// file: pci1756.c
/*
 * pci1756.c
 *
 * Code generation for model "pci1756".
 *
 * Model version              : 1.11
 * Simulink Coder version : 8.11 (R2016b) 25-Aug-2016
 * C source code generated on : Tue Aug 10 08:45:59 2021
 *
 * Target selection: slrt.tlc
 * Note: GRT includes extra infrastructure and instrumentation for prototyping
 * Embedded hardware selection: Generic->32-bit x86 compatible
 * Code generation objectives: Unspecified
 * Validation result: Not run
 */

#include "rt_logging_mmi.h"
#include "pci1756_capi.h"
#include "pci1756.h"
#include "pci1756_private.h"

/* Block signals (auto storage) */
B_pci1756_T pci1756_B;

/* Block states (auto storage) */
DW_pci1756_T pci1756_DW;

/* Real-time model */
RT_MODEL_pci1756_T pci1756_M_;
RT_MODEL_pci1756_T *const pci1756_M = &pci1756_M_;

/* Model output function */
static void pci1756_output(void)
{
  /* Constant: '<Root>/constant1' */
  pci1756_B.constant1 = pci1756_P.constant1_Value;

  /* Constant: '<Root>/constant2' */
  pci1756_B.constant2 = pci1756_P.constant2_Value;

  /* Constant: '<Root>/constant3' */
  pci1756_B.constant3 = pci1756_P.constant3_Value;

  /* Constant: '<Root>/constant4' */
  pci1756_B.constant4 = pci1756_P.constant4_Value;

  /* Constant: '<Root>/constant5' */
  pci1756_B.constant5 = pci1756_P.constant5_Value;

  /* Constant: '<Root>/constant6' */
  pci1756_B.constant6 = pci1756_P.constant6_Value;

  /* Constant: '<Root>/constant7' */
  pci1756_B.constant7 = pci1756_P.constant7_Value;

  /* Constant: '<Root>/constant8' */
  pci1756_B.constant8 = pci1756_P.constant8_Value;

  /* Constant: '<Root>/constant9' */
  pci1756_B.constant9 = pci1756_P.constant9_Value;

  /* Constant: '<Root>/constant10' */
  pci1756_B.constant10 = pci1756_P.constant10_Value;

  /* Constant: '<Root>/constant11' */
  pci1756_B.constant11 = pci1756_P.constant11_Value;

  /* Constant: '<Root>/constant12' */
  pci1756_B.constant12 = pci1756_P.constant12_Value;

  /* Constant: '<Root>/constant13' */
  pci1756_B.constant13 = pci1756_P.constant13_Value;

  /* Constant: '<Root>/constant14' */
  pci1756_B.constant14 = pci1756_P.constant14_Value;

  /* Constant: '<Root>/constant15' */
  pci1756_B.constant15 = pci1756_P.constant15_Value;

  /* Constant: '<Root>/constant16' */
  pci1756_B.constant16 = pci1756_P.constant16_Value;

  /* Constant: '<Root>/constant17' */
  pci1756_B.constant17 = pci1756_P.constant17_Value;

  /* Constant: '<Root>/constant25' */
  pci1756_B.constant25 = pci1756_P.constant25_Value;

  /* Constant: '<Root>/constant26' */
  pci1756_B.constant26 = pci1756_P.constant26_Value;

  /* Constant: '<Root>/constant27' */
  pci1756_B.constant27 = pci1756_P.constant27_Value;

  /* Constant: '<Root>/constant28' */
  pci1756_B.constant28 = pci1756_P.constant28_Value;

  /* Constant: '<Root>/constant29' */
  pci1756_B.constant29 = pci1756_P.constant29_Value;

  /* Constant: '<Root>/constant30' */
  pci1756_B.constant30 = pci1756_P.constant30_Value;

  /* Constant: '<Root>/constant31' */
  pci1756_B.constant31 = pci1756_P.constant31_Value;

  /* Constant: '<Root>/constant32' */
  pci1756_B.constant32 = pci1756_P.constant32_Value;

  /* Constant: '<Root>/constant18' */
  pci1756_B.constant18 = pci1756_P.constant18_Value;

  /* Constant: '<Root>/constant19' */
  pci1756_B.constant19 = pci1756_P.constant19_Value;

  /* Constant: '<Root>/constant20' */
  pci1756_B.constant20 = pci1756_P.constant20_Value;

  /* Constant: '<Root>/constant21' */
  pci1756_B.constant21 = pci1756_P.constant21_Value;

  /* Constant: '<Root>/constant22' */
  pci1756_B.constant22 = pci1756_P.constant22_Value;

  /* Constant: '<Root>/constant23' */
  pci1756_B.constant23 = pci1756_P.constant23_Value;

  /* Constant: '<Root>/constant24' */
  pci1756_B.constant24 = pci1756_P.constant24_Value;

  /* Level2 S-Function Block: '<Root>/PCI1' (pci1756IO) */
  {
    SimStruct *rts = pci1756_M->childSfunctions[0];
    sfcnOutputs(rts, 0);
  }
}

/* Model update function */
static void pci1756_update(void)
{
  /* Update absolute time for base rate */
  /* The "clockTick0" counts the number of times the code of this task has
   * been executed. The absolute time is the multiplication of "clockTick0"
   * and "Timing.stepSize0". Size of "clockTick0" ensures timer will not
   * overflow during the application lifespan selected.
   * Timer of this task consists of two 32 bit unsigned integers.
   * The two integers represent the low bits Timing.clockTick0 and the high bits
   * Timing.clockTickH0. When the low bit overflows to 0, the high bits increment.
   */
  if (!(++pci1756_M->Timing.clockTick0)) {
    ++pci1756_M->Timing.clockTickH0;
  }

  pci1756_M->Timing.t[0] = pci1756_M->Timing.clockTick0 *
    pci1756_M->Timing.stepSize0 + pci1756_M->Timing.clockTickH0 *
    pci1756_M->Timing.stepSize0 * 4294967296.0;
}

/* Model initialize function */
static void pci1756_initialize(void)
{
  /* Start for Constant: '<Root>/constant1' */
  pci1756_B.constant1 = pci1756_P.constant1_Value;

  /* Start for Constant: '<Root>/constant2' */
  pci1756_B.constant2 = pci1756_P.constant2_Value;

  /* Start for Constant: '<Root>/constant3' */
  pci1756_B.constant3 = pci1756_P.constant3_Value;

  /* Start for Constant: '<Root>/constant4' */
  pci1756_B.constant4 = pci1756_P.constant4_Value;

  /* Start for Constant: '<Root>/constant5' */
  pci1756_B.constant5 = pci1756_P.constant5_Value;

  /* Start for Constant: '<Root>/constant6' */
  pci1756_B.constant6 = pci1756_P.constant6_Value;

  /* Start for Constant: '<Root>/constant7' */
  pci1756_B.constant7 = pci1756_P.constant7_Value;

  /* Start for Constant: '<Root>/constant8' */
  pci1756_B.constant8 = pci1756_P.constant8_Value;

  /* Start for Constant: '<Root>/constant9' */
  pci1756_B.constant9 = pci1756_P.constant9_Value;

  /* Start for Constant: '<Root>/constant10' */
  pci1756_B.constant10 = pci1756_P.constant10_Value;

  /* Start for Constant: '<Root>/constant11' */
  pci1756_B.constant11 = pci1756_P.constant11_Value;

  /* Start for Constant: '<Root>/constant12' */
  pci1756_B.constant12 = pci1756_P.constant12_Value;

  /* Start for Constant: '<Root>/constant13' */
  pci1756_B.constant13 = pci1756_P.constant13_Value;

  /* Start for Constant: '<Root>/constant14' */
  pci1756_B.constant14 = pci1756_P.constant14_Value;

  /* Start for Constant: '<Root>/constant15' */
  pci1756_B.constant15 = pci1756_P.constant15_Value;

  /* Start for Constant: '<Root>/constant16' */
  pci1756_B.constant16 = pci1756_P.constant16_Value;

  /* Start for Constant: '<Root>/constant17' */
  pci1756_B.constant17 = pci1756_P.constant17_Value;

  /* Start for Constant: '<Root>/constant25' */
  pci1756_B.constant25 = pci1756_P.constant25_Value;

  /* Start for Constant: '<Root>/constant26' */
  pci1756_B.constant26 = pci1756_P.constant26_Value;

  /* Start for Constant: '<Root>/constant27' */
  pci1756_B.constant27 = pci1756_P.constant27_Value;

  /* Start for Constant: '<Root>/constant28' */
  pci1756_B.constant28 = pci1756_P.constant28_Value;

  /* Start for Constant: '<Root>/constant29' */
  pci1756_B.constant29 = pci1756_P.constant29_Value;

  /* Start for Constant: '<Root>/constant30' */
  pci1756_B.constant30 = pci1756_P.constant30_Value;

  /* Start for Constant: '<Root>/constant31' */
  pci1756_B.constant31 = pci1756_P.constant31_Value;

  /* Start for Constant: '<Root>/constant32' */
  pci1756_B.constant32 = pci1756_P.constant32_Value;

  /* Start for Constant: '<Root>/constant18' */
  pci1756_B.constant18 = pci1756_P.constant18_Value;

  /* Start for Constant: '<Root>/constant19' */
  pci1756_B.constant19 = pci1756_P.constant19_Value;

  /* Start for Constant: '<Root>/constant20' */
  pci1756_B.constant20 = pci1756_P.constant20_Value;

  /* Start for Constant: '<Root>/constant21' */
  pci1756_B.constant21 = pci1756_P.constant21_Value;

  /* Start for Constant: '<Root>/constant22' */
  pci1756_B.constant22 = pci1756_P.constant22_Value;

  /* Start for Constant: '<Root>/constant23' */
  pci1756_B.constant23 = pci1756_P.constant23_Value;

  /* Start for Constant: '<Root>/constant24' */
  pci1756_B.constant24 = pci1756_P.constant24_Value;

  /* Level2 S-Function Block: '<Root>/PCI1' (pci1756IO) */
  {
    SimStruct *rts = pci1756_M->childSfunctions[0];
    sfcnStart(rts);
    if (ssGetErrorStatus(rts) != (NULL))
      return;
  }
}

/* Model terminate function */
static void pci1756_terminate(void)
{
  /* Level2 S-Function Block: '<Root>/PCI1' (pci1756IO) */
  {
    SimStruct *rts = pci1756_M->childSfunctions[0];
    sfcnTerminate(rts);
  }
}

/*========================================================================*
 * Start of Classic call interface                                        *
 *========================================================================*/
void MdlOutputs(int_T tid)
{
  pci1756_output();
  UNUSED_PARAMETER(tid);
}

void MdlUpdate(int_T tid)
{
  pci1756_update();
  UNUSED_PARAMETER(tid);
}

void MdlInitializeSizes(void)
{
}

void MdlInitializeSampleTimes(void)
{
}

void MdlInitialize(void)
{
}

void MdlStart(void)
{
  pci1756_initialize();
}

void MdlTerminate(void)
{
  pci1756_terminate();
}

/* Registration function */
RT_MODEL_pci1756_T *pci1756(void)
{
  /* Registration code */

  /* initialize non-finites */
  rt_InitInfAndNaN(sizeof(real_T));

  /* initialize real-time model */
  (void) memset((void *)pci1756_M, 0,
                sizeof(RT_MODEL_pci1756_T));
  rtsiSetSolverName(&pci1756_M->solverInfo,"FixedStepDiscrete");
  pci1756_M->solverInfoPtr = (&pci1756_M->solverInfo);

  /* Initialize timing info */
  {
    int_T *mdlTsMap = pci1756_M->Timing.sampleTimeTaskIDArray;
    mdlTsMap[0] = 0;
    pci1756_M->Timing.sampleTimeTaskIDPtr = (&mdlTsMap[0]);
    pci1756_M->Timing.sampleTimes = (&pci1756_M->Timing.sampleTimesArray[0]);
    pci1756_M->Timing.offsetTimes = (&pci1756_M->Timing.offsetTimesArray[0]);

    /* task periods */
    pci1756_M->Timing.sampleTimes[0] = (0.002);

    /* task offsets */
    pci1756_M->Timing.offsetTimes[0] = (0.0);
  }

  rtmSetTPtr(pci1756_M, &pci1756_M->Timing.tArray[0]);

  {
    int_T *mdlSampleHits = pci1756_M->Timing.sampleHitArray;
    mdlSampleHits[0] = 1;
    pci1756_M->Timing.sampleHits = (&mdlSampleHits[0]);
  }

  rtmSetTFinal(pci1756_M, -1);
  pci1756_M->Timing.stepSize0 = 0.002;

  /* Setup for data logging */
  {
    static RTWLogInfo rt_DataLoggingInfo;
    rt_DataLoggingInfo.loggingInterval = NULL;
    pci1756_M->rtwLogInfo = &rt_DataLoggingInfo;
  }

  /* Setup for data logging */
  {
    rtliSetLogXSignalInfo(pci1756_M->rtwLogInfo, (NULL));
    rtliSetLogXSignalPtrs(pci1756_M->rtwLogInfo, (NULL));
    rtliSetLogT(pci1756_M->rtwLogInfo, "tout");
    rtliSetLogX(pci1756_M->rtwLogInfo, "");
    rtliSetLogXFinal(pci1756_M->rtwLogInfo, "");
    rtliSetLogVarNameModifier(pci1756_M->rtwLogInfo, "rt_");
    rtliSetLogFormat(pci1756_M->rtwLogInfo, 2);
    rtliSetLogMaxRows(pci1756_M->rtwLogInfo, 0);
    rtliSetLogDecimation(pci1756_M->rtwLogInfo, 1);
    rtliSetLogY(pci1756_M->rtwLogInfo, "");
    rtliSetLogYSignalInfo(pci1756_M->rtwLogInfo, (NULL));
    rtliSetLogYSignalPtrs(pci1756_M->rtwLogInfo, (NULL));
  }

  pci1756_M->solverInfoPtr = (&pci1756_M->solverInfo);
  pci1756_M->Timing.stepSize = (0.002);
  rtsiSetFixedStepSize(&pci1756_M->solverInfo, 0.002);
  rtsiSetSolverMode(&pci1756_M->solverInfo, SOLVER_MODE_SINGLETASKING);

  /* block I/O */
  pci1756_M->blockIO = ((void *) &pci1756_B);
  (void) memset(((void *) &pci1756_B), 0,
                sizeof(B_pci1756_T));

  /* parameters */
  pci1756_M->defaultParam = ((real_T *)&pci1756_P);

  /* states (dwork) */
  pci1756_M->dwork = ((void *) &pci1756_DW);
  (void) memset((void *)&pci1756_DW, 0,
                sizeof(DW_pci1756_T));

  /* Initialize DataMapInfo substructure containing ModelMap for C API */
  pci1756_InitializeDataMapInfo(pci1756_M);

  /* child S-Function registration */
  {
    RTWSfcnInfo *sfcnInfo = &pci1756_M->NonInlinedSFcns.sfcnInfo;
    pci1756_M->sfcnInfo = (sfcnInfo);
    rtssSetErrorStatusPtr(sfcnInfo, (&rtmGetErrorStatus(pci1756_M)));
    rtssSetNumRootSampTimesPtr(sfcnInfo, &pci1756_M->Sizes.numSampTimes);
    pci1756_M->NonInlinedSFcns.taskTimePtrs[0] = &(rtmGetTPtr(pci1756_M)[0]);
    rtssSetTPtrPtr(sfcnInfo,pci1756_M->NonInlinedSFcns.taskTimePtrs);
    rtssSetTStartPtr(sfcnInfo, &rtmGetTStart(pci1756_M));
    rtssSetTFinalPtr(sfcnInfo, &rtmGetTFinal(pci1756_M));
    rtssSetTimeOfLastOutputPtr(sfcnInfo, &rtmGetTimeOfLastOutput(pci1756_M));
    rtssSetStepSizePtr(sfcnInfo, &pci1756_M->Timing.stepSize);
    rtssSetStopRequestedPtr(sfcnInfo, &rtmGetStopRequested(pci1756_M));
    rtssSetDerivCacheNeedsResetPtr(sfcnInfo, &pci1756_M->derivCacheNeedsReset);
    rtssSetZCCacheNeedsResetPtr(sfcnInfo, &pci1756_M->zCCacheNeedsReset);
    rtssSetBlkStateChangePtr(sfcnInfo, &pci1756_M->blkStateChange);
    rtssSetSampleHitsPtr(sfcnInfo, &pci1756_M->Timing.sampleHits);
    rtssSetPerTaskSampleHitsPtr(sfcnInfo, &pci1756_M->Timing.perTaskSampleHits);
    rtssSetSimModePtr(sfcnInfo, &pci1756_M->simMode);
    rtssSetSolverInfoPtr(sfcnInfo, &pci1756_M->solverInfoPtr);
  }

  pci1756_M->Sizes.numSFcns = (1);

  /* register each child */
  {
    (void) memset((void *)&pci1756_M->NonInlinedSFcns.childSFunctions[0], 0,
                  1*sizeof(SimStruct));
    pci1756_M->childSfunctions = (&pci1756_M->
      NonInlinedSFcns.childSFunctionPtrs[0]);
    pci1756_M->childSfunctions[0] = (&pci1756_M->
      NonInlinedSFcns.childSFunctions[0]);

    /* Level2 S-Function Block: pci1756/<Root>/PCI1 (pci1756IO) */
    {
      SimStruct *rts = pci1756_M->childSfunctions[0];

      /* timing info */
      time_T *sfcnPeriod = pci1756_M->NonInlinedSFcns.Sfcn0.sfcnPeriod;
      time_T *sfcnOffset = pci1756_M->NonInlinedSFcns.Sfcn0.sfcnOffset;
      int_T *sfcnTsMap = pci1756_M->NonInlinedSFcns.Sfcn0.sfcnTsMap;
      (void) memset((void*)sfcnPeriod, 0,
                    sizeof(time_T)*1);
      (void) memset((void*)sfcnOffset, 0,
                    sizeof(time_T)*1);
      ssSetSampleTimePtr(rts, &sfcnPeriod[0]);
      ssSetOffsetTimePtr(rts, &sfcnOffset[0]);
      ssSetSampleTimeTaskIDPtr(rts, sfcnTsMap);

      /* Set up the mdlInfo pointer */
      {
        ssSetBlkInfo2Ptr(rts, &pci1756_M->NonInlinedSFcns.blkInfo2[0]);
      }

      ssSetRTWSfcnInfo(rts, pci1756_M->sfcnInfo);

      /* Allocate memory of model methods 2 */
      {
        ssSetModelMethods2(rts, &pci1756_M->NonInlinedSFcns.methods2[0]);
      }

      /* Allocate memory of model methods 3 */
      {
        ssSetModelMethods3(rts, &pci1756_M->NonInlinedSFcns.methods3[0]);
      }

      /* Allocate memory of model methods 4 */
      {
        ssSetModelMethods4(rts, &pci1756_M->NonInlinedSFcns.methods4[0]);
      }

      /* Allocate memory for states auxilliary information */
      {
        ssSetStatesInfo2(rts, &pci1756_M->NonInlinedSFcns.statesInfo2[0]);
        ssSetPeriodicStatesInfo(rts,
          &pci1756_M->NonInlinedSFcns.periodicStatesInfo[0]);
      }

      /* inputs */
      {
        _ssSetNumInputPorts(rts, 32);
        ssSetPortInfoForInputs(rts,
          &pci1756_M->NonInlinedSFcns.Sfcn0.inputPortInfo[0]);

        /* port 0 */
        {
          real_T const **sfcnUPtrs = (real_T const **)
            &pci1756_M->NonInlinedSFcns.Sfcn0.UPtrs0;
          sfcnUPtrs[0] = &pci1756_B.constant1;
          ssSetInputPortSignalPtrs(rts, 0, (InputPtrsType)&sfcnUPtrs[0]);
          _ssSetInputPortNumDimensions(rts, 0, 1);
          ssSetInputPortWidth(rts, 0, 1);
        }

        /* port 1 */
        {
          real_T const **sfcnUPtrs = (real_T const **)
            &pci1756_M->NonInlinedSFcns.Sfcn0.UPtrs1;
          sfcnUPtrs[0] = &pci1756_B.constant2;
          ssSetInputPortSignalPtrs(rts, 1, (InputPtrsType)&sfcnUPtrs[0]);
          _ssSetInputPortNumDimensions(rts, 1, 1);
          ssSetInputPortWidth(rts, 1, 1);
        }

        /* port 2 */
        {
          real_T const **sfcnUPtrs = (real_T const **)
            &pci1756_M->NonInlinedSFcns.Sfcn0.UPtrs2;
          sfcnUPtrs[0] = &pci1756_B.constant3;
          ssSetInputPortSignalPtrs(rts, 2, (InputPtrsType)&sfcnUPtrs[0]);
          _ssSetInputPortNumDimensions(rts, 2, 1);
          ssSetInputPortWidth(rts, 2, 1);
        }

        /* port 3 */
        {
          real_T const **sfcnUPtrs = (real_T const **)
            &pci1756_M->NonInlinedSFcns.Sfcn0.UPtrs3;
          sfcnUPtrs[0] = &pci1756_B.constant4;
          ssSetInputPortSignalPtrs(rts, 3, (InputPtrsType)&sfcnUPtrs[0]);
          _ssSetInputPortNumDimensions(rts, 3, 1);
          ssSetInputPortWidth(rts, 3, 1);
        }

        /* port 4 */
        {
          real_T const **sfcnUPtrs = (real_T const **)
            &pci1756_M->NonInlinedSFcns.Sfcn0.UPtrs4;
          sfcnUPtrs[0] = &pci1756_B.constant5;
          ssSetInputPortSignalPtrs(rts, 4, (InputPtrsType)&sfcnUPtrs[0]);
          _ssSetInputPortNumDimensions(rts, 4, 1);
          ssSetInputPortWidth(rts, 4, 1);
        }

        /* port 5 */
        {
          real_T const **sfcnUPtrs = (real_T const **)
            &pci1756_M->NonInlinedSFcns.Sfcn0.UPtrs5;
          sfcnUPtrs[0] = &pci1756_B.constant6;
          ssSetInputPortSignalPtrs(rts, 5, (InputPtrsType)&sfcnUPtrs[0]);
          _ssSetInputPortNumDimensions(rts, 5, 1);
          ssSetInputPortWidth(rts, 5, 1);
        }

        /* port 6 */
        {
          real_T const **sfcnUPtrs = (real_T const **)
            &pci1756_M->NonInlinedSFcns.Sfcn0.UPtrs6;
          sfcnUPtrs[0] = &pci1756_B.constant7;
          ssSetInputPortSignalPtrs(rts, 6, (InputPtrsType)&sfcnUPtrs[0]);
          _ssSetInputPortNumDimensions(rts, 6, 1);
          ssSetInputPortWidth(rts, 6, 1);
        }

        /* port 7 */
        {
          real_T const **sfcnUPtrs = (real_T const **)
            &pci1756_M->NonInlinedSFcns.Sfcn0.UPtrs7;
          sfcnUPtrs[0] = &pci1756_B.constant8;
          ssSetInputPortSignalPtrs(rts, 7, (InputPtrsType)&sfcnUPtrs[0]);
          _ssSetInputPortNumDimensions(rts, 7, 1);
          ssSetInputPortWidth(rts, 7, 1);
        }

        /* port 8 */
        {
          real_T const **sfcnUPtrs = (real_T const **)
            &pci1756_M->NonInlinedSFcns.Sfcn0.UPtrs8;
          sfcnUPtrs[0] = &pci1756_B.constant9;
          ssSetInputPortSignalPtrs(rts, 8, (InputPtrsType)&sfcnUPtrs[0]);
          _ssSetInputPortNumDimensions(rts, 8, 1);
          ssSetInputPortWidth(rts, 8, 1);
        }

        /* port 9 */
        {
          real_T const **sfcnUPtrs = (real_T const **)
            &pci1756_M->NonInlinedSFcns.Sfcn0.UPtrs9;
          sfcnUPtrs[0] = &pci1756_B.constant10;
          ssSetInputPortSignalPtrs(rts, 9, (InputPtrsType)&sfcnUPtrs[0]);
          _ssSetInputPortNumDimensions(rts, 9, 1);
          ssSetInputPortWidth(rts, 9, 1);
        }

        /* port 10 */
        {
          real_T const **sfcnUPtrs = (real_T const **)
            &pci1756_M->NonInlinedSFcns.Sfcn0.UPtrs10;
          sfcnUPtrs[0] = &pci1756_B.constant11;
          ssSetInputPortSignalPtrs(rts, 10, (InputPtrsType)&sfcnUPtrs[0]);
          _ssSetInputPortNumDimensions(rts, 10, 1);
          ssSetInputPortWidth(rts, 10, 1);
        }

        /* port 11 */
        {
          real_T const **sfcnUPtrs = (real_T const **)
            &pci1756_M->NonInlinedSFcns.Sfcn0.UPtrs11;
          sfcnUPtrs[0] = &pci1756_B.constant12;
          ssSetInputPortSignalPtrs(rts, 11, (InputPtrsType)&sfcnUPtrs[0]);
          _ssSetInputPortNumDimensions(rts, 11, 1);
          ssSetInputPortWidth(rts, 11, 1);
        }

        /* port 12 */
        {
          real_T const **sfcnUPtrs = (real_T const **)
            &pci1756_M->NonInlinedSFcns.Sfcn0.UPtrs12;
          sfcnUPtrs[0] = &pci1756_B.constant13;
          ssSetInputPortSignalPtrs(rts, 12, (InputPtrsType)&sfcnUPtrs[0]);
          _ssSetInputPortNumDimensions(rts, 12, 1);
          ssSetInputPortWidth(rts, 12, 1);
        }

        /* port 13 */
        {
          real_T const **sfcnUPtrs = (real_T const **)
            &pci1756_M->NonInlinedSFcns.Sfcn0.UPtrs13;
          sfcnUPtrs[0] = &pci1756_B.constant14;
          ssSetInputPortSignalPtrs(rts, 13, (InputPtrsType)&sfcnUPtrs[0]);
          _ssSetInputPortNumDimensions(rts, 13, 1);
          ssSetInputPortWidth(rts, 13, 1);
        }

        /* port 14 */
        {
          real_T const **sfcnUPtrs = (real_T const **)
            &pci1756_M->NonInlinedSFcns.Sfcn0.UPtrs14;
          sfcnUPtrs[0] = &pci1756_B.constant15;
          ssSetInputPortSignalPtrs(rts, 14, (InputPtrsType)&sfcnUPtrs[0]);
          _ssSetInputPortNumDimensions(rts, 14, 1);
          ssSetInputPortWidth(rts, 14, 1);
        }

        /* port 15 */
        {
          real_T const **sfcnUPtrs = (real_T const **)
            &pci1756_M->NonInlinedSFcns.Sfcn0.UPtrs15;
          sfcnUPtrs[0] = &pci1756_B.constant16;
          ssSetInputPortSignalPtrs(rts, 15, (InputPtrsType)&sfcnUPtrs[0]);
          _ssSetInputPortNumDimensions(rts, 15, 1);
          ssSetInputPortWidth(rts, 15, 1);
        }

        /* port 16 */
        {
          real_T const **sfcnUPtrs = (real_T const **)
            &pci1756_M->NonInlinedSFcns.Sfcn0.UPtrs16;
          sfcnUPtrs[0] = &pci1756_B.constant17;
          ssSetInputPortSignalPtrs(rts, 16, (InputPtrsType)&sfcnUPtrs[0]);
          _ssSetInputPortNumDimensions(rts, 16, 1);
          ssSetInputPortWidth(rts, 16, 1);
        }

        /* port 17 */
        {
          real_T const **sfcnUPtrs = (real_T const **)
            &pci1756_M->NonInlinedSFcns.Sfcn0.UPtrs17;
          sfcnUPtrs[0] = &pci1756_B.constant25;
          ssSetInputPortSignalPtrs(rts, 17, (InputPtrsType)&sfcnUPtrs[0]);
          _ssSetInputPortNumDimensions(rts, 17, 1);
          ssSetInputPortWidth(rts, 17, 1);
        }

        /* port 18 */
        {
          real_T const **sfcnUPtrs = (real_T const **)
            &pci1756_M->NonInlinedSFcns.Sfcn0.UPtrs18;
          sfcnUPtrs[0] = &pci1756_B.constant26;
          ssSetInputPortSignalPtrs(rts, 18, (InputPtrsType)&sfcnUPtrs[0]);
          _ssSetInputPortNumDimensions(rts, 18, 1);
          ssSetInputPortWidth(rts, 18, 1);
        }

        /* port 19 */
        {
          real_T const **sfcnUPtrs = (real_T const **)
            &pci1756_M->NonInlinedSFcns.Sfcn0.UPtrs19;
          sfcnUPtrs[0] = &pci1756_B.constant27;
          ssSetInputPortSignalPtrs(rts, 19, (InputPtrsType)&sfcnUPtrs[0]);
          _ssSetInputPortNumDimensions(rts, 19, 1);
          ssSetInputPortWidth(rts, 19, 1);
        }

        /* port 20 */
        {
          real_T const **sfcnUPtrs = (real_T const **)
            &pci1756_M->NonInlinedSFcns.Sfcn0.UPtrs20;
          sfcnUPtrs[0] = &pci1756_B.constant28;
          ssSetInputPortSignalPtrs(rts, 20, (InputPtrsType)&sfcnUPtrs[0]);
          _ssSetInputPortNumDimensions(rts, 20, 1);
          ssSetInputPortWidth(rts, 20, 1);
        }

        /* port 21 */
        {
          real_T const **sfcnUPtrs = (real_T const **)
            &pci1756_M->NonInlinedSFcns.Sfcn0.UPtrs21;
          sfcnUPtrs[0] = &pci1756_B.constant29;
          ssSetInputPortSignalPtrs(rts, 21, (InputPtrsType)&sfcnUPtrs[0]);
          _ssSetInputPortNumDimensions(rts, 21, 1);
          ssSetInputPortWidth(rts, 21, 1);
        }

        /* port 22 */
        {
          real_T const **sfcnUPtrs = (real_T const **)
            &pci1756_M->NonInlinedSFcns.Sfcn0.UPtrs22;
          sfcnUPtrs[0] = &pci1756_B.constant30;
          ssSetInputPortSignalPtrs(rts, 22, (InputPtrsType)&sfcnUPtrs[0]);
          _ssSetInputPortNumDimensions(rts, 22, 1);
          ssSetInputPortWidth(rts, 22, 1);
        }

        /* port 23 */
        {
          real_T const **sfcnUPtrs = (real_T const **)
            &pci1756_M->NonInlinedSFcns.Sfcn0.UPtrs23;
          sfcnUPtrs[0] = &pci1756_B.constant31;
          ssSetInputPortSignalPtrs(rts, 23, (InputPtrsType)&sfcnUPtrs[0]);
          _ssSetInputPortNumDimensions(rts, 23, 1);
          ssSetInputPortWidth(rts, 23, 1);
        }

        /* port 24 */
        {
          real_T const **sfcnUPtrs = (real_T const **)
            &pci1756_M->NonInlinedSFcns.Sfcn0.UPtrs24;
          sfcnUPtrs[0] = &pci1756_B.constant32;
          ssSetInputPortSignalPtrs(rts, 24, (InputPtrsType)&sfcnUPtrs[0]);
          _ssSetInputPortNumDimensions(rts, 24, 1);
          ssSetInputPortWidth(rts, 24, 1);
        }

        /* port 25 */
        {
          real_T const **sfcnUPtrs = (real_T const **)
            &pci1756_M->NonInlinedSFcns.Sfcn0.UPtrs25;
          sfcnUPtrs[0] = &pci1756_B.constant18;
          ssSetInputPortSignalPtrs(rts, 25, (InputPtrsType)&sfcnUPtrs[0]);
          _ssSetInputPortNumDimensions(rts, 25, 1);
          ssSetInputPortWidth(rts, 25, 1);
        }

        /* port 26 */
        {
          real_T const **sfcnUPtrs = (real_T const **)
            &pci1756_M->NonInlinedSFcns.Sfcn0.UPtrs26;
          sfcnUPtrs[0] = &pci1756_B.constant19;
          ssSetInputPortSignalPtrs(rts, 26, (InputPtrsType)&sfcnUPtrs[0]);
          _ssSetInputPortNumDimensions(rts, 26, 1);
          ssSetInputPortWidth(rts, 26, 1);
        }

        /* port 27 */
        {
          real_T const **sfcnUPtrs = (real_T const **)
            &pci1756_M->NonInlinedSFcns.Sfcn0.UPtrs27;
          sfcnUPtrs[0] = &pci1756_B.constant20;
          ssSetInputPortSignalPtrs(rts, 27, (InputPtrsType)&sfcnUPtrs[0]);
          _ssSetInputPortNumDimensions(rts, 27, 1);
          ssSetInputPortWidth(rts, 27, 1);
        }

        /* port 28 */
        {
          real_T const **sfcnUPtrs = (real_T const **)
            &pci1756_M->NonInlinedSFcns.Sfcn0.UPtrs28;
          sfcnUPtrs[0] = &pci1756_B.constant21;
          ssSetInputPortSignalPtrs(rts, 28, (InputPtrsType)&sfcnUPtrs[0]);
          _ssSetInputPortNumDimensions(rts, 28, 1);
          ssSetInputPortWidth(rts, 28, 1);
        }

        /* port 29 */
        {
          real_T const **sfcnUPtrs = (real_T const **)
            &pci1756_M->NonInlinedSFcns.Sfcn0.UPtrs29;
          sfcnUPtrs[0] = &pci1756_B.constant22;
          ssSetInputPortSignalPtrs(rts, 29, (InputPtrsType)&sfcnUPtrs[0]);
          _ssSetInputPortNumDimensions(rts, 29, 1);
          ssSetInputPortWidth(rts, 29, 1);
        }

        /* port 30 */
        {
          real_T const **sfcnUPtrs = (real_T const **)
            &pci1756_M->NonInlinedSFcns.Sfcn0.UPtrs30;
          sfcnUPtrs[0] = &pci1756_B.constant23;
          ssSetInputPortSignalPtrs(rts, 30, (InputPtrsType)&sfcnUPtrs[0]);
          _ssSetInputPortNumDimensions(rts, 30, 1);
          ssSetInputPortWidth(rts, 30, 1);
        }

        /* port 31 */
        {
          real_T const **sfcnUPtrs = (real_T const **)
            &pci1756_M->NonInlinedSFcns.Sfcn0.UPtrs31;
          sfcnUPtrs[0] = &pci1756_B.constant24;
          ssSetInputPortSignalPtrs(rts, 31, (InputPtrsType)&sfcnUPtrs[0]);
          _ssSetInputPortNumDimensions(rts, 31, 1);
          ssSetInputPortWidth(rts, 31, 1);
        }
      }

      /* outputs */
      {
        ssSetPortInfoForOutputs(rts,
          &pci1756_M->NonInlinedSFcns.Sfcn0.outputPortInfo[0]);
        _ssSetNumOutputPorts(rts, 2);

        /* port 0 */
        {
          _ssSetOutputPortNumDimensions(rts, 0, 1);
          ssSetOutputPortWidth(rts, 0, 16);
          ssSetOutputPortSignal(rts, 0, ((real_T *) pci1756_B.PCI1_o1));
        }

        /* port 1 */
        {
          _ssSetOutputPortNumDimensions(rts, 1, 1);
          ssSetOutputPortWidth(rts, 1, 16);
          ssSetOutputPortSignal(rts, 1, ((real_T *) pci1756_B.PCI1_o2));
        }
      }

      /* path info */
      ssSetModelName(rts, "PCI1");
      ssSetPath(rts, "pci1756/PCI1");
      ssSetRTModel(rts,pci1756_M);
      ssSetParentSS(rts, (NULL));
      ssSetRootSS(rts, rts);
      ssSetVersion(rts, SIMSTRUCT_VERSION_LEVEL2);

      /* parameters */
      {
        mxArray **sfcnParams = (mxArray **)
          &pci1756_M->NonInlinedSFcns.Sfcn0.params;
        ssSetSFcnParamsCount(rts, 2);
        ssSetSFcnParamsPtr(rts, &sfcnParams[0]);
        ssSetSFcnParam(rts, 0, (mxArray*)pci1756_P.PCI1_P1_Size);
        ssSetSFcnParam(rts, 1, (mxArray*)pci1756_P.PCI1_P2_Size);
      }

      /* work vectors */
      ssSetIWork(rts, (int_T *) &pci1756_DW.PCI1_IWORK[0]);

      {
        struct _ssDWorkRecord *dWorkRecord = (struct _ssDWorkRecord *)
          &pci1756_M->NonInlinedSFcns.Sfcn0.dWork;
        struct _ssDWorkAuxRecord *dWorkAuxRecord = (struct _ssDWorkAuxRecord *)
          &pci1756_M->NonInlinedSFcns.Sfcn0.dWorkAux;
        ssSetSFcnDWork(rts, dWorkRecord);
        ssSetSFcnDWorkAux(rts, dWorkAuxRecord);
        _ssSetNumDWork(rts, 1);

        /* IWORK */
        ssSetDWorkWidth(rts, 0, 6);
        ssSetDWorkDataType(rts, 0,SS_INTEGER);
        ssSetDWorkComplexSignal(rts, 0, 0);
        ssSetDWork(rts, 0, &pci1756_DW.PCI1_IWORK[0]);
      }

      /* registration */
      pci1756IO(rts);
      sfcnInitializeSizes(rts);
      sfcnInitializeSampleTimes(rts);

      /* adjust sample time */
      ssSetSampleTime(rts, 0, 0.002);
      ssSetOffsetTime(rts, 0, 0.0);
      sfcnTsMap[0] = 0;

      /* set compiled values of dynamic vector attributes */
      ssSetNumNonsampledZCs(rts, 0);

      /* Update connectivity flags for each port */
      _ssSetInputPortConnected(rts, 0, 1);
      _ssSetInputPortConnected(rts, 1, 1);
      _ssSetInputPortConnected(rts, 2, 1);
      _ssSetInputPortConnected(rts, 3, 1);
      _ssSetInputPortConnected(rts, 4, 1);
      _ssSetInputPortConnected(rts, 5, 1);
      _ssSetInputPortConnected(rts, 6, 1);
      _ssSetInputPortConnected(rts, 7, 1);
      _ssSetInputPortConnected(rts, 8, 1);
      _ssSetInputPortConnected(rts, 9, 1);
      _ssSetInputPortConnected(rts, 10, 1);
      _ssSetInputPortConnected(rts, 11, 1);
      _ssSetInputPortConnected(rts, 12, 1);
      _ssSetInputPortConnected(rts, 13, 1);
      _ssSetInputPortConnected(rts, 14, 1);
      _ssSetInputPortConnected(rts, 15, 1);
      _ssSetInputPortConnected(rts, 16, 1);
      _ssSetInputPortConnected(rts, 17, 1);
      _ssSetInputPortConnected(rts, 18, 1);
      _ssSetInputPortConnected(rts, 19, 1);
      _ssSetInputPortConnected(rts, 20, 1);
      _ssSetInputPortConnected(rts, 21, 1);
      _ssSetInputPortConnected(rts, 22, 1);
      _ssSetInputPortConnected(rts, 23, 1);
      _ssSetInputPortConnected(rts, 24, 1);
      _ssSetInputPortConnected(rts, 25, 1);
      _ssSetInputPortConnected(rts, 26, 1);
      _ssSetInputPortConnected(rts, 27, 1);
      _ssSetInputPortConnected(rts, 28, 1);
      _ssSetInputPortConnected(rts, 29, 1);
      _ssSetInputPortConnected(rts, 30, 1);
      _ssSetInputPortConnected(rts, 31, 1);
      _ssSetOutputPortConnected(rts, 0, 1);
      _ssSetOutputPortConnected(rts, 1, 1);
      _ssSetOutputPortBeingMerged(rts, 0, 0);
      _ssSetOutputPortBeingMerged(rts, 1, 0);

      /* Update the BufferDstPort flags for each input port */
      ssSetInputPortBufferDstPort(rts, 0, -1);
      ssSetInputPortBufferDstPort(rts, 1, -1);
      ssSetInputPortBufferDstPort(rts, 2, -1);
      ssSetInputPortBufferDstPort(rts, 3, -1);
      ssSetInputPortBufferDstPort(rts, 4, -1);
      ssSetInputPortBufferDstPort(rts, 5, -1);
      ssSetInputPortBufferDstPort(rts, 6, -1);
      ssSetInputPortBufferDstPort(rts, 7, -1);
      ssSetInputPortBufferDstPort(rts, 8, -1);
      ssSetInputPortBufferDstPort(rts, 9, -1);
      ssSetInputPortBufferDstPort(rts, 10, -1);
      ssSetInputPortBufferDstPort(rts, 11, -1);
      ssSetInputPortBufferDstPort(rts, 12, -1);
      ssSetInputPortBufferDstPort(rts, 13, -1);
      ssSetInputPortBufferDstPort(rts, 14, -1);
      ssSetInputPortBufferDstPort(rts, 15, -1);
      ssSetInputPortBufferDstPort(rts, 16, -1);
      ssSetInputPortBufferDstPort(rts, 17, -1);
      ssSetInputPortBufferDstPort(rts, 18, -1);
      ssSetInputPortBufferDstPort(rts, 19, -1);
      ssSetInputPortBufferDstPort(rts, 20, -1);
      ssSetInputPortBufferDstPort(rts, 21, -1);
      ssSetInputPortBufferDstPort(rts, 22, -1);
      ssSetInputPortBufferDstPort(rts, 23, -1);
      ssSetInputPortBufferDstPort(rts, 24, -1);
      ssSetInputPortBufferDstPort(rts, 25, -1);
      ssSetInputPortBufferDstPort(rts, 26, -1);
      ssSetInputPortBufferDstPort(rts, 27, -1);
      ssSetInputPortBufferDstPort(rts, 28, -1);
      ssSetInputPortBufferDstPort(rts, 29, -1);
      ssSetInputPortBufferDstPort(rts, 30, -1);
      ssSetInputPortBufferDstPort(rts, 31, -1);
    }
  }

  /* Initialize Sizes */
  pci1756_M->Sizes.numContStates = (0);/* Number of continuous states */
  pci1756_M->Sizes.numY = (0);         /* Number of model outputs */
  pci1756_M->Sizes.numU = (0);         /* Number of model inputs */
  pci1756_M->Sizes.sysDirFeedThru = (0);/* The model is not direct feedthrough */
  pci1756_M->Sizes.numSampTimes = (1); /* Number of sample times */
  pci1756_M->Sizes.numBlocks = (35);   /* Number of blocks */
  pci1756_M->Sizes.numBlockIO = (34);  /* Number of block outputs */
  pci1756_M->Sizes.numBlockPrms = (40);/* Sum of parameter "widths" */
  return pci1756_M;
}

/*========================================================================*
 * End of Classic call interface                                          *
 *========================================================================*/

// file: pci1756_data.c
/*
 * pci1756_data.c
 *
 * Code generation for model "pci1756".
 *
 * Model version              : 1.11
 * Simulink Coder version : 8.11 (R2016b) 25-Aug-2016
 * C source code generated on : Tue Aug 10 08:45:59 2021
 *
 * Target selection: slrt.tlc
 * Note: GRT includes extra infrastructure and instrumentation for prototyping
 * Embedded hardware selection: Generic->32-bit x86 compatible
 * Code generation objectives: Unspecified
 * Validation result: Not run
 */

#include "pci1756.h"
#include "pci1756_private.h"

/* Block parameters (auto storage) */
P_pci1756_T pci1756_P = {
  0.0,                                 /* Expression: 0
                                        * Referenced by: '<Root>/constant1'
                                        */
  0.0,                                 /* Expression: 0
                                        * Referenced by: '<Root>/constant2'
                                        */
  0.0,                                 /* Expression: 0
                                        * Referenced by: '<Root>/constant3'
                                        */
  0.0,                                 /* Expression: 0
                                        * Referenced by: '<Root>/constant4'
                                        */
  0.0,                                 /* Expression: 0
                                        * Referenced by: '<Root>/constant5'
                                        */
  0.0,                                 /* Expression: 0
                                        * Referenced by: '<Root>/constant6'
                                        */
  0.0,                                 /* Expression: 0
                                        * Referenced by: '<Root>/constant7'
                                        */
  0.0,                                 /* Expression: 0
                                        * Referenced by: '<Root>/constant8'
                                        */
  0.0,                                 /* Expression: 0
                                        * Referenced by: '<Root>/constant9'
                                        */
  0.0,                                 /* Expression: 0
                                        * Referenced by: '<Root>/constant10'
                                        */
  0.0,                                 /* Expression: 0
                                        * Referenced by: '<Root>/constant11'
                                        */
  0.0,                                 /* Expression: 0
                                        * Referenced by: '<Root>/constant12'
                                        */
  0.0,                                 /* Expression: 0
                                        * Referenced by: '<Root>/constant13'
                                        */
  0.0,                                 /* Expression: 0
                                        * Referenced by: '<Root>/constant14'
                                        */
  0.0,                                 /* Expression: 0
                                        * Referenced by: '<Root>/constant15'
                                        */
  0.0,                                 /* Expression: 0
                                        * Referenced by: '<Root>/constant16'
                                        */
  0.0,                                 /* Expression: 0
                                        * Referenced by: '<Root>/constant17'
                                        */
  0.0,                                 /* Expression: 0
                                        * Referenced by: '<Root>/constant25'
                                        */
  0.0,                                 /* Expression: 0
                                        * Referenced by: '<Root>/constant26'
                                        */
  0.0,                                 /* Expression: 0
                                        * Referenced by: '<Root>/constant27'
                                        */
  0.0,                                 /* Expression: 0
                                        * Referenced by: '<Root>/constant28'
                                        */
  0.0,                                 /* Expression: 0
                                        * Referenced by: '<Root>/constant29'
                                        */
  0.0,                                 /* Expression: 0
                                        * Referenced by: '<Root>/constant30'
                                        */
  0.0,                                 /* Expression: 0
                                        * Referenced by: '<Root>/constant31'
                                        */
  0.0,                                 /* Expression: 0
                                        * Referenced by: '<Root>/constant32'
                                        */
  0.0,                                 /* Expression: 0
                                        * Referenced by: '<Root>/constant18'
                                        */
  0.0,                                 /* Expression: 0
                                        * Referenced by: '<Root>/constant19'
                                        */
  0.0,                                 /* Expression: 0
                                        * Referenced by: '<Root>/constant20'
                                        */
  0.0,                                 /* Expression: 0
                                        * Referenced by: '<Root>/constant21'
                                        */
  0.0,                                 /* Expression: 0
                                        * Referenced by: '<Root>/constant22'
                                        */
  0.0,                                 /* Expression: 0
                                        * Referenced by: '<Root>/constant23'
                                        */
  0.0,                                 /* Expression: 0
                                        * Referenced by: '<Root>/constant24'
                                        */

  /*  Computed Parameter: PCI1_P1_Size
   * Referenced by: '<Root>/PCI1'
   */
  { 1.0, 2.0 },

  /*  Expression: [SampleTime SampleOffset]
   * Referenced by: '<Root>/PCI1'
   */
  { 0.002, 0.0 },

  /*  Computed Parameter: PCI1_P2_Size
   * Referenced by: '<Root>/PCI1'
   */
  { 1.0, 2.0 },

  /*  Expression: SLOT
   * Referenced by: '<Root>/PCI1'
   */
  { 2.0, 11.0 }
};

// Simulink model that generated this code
simulink model "pci1756"  (R2016b)
settings: Solver=ode4  StartTime=0.0  StopTime=inf  FixedStep=0.002  RelTol=1e-3  EnableMultiTasking=on

== system pci1756 ==
  Display : Display
  Display1 : Display
  PCI1 : S-Function  FunctionName=pci1756IO  Parameters=[SampleTime SampleOffset], SLOT  SFunctionDeploymentMode=off  EnableBusSupport=off  mask(PCI1756){Sample=0.002, SLOT=[2 11]}
      mask prompts: Sample "Sample time:"
      mask help:
      | PCI-1756
      | Advantech
      | Digital Input&Output
      mask init:
      | SampleTime =0.002; SampleOffset=0;
  constant{1..32} (32 alike) : Constant  Value=0
  wires:
  constant2/1 -> PCI1/2
  constant3/1 -> PCI1/3
  constant4/1 -> PCI1/4
  constant5/1 -> PCI1/5
  constant6/1 -> PCI1/6
  constant7/1 -> PCI1/7
  constant8/1 -> PCI1/8
  constant9/1 -> PCI1/9
  constant10/1 -> PCI1/10
  constant11/1 -> PCI1/11
  constant12/1 -> PCI1/12
  constant13/1 -> PCI1/13
  constant14/1 -> PCI1/14
  constant15/1 -> PCI1/15
  constant16/1 -> PCI1/16
  constant17/1 -> PCI1/17
  constant25/1 -> PCI1/18
  constant26/1 -> PCI1/19
  constant27/1 -> PCI1/20
  constant28/1 -> PCI1/21
  constant29/1 -> PCI1/22
  constant30/1 -> PCI1/23
  constant31/1 -> PCI1/24
  constant32/1 -> PCI1/25
  constant18/1 -> PCI1/26
  constant19/1 -> PCI1/27
  constant20/1 -> PCI1/28
  constant21/1 -> PCI1/29
  constant22/1 -> PCI1/30
  constant23/1 -> PCI1/31
  constant24/1 -> PCI1/32
  PCI1/1 -> Display/1
  constant1/1 -> PCI1/1
  PCI1/2 -> Display1/1
